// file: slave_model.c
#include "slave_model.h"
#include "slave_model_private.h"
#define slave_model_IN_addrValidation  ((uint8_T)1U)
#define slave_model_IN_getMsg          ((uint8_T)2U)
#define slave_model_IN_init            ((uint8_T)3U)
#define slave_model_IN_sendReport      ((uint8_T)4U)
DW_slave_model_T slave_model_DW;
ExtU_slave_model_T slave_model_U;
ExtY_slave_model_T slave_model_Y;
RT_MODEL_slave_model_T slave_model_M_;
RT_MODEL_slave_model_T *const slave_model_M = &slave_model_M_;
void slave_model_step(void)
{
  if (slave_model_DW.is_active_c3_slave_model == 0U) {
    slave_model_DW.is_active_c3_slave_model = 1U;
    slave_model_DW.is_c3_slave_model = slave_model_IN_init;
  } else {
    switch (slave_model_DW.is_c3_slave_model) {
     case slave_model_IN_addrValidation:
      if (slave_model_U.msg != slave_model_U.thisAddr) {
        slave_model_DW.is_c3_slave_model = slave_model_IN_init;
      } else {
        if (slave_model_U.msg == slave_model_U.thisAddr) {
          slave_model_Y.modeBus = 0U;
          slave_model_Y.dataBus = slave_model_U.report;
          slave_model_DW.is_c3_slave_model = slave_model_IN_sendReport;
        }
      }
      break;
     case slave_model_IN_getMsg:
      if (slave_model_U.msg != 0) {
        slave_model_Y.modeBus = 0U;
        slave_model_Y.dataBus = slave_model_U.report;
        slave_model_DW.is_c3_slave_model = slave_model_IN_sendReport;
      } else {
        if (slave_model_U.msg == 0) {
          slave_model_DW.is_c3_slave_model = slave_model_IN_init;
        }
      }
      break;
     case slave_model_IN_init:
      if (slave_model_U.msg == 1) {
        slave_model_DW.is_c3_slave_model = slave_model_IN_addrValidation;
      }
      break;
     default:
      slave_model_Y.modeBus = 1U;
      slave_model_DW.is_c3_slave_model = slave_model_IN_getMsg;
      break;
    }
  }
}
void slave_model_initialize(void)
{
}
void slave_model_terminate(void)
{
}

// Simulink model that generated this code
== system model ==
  msg : Inport
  report : Inport
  thisAddr : Inport
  modeBus : Outport  <- 1: Stateflowchart#1
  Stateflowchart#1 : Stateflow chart  <- 1: msg, 2: report, 3: thisAddr
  dataBus : Outport  <- 1: Stateflowchart#1/2
== stateflow chart Stateflowchart#1 ==
  state init
  state addrValidation
  state sendReport
  state getMsg
  addrValidation -> sendReport [order 2] : [msg==thisAddr]{modeBus=0,dataBus=report}
  init -> addrValidation : [msg==1]
  (default) -> init
  sendReport -> getMsg : {modeBus=1}
  getMsg -> init [order 2] : [msg==0]
  addrValidation -> init [order 1] : [msg~=thisAddr]
  getMsg -> sendReport [order 1] : [msg~=0]{modeBus=0; dataBus=report}
  data: msg input uint8; modeBus output uint8; dataBus output uint8; report input uint8; thisAddr input uint8
